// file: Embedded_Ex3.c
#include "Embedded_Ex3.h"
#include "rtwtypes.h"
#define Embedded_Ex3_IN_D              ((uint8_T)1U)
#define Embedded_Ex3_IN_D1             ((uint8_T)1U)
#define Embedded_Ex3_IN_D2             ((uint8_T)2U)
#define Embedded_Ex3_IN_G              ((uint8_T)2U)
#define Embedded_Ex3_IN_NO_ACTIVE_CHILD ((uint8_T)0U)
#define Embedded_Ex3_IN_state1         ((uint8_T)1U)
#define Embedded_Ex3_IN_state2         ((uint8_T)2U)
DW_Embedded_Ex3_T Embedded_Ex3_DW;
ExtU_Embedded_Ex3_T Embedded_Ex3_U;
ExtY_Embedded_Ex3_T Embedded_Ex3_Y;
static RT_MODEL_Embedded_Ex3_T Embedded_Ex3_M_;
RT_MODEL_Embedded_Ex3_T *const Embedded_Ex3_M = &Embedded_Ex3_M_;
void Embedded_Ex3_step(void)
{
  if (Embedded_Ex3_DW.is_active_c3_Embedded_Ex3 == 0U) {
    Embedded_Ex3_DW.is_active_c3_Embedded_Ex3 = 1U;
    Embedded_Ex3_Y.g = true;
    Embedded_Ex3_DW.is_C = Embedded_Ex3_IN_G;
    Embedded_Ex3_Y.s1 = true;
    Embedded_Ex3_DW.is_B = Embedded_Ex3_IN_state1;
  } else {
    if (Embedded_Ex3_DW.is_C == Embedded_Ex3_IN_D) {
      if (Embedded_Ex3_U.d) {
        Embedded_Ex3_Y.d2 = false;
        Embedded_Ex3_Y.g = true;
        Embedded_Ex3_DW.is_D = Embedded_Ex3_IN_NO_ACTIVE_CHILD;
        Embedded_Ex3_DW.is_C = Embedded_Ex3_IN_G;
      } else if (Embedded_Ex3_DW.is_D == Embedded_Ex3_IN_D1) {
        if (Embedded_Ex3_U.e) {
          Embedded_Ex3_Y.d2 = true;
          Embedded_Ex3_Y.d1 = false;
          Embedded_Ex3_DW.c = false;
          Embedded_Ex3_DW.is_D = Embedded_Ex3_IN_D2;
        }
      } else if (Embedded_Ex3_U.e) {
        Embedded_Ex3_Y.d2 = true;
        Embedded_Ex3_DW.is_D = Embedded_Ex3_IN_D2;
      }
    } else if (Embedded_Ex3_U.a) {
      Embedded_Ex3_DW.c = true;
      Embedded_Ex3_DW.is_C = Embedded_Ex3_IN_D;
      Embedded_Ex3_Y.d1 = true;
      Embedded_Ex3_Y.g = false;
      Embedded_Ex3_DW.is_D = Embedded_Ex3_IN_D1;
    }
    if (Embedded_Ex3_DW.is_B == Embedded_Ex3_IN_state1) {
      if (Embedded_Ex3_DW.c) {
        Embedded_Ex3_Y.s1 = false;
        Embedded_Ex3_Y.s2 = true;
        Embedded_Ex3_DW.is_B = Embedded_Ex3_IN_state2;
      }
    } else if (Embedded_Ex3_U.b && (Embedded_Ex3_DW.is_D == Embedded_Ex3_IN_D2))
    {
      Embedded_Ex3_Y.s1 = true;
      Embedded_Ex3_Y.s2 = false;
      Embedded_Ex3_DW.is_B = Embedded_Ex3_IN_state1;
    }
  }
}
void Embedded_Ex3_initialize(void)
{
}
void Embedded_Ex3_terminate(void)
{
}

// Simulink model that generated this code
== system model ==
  Inport#1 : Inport
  Inport#2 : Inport
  Inport#3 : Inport
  Inport#4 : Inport
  Outport#1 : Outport  <- 1: Stateflowchart#1
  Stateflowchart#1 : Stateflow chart  <- 1: Inport#1, 2: Inport#2, 3: Inport#3, 4: Inport#4
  d2 : Outport  <- 1: Stateflowchart#1/4
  d1 : Outport  <- 1: Stateflowchart#1/5
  s1 : Outport  <- 1: Stateflowchart#1/2
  s2 : Outport  <- 1: Stateflowchart#1/3
== stateflow chart Stateflowchart#1 ==
  state B [parallel]
    settings: executionOrder=2
    state state1
    state state2
    (default) -> state1 : {Sstate1=true;}
    state1 -> state2 : [c==true]{Sstate1=false;Sstate2=true;}
    state2 -> state1 : [Sb == true && in(C.D.D2)]{Sstate1=true;Sstate2=false;}
  state C [parallel]
    settings: executionOrder=1
    state D
      state D1
      state D2
      (default) -> D1 : {SD1=true;SG=false;}
      D1 -> D2 : [Se==true]{SD2 = true;SD1= false;c = false;}
      D2 -> D2 : [Se==true]{SD2= true;}
    state G
    G -> D : [Sa==true]{c = true;SG=false;}
    (default) -> G : {SG=true;}
    D -> G : [Sd==true]{SD2=false;SG=true;}
  data: c local size=1 =false; SG output =false; Sstate1 output =false; Sstate2 output =false; Sa input boolean; Sb input boolean; Sd input boolean; Se input boolean; SD2 output =false; SD1 output =false
